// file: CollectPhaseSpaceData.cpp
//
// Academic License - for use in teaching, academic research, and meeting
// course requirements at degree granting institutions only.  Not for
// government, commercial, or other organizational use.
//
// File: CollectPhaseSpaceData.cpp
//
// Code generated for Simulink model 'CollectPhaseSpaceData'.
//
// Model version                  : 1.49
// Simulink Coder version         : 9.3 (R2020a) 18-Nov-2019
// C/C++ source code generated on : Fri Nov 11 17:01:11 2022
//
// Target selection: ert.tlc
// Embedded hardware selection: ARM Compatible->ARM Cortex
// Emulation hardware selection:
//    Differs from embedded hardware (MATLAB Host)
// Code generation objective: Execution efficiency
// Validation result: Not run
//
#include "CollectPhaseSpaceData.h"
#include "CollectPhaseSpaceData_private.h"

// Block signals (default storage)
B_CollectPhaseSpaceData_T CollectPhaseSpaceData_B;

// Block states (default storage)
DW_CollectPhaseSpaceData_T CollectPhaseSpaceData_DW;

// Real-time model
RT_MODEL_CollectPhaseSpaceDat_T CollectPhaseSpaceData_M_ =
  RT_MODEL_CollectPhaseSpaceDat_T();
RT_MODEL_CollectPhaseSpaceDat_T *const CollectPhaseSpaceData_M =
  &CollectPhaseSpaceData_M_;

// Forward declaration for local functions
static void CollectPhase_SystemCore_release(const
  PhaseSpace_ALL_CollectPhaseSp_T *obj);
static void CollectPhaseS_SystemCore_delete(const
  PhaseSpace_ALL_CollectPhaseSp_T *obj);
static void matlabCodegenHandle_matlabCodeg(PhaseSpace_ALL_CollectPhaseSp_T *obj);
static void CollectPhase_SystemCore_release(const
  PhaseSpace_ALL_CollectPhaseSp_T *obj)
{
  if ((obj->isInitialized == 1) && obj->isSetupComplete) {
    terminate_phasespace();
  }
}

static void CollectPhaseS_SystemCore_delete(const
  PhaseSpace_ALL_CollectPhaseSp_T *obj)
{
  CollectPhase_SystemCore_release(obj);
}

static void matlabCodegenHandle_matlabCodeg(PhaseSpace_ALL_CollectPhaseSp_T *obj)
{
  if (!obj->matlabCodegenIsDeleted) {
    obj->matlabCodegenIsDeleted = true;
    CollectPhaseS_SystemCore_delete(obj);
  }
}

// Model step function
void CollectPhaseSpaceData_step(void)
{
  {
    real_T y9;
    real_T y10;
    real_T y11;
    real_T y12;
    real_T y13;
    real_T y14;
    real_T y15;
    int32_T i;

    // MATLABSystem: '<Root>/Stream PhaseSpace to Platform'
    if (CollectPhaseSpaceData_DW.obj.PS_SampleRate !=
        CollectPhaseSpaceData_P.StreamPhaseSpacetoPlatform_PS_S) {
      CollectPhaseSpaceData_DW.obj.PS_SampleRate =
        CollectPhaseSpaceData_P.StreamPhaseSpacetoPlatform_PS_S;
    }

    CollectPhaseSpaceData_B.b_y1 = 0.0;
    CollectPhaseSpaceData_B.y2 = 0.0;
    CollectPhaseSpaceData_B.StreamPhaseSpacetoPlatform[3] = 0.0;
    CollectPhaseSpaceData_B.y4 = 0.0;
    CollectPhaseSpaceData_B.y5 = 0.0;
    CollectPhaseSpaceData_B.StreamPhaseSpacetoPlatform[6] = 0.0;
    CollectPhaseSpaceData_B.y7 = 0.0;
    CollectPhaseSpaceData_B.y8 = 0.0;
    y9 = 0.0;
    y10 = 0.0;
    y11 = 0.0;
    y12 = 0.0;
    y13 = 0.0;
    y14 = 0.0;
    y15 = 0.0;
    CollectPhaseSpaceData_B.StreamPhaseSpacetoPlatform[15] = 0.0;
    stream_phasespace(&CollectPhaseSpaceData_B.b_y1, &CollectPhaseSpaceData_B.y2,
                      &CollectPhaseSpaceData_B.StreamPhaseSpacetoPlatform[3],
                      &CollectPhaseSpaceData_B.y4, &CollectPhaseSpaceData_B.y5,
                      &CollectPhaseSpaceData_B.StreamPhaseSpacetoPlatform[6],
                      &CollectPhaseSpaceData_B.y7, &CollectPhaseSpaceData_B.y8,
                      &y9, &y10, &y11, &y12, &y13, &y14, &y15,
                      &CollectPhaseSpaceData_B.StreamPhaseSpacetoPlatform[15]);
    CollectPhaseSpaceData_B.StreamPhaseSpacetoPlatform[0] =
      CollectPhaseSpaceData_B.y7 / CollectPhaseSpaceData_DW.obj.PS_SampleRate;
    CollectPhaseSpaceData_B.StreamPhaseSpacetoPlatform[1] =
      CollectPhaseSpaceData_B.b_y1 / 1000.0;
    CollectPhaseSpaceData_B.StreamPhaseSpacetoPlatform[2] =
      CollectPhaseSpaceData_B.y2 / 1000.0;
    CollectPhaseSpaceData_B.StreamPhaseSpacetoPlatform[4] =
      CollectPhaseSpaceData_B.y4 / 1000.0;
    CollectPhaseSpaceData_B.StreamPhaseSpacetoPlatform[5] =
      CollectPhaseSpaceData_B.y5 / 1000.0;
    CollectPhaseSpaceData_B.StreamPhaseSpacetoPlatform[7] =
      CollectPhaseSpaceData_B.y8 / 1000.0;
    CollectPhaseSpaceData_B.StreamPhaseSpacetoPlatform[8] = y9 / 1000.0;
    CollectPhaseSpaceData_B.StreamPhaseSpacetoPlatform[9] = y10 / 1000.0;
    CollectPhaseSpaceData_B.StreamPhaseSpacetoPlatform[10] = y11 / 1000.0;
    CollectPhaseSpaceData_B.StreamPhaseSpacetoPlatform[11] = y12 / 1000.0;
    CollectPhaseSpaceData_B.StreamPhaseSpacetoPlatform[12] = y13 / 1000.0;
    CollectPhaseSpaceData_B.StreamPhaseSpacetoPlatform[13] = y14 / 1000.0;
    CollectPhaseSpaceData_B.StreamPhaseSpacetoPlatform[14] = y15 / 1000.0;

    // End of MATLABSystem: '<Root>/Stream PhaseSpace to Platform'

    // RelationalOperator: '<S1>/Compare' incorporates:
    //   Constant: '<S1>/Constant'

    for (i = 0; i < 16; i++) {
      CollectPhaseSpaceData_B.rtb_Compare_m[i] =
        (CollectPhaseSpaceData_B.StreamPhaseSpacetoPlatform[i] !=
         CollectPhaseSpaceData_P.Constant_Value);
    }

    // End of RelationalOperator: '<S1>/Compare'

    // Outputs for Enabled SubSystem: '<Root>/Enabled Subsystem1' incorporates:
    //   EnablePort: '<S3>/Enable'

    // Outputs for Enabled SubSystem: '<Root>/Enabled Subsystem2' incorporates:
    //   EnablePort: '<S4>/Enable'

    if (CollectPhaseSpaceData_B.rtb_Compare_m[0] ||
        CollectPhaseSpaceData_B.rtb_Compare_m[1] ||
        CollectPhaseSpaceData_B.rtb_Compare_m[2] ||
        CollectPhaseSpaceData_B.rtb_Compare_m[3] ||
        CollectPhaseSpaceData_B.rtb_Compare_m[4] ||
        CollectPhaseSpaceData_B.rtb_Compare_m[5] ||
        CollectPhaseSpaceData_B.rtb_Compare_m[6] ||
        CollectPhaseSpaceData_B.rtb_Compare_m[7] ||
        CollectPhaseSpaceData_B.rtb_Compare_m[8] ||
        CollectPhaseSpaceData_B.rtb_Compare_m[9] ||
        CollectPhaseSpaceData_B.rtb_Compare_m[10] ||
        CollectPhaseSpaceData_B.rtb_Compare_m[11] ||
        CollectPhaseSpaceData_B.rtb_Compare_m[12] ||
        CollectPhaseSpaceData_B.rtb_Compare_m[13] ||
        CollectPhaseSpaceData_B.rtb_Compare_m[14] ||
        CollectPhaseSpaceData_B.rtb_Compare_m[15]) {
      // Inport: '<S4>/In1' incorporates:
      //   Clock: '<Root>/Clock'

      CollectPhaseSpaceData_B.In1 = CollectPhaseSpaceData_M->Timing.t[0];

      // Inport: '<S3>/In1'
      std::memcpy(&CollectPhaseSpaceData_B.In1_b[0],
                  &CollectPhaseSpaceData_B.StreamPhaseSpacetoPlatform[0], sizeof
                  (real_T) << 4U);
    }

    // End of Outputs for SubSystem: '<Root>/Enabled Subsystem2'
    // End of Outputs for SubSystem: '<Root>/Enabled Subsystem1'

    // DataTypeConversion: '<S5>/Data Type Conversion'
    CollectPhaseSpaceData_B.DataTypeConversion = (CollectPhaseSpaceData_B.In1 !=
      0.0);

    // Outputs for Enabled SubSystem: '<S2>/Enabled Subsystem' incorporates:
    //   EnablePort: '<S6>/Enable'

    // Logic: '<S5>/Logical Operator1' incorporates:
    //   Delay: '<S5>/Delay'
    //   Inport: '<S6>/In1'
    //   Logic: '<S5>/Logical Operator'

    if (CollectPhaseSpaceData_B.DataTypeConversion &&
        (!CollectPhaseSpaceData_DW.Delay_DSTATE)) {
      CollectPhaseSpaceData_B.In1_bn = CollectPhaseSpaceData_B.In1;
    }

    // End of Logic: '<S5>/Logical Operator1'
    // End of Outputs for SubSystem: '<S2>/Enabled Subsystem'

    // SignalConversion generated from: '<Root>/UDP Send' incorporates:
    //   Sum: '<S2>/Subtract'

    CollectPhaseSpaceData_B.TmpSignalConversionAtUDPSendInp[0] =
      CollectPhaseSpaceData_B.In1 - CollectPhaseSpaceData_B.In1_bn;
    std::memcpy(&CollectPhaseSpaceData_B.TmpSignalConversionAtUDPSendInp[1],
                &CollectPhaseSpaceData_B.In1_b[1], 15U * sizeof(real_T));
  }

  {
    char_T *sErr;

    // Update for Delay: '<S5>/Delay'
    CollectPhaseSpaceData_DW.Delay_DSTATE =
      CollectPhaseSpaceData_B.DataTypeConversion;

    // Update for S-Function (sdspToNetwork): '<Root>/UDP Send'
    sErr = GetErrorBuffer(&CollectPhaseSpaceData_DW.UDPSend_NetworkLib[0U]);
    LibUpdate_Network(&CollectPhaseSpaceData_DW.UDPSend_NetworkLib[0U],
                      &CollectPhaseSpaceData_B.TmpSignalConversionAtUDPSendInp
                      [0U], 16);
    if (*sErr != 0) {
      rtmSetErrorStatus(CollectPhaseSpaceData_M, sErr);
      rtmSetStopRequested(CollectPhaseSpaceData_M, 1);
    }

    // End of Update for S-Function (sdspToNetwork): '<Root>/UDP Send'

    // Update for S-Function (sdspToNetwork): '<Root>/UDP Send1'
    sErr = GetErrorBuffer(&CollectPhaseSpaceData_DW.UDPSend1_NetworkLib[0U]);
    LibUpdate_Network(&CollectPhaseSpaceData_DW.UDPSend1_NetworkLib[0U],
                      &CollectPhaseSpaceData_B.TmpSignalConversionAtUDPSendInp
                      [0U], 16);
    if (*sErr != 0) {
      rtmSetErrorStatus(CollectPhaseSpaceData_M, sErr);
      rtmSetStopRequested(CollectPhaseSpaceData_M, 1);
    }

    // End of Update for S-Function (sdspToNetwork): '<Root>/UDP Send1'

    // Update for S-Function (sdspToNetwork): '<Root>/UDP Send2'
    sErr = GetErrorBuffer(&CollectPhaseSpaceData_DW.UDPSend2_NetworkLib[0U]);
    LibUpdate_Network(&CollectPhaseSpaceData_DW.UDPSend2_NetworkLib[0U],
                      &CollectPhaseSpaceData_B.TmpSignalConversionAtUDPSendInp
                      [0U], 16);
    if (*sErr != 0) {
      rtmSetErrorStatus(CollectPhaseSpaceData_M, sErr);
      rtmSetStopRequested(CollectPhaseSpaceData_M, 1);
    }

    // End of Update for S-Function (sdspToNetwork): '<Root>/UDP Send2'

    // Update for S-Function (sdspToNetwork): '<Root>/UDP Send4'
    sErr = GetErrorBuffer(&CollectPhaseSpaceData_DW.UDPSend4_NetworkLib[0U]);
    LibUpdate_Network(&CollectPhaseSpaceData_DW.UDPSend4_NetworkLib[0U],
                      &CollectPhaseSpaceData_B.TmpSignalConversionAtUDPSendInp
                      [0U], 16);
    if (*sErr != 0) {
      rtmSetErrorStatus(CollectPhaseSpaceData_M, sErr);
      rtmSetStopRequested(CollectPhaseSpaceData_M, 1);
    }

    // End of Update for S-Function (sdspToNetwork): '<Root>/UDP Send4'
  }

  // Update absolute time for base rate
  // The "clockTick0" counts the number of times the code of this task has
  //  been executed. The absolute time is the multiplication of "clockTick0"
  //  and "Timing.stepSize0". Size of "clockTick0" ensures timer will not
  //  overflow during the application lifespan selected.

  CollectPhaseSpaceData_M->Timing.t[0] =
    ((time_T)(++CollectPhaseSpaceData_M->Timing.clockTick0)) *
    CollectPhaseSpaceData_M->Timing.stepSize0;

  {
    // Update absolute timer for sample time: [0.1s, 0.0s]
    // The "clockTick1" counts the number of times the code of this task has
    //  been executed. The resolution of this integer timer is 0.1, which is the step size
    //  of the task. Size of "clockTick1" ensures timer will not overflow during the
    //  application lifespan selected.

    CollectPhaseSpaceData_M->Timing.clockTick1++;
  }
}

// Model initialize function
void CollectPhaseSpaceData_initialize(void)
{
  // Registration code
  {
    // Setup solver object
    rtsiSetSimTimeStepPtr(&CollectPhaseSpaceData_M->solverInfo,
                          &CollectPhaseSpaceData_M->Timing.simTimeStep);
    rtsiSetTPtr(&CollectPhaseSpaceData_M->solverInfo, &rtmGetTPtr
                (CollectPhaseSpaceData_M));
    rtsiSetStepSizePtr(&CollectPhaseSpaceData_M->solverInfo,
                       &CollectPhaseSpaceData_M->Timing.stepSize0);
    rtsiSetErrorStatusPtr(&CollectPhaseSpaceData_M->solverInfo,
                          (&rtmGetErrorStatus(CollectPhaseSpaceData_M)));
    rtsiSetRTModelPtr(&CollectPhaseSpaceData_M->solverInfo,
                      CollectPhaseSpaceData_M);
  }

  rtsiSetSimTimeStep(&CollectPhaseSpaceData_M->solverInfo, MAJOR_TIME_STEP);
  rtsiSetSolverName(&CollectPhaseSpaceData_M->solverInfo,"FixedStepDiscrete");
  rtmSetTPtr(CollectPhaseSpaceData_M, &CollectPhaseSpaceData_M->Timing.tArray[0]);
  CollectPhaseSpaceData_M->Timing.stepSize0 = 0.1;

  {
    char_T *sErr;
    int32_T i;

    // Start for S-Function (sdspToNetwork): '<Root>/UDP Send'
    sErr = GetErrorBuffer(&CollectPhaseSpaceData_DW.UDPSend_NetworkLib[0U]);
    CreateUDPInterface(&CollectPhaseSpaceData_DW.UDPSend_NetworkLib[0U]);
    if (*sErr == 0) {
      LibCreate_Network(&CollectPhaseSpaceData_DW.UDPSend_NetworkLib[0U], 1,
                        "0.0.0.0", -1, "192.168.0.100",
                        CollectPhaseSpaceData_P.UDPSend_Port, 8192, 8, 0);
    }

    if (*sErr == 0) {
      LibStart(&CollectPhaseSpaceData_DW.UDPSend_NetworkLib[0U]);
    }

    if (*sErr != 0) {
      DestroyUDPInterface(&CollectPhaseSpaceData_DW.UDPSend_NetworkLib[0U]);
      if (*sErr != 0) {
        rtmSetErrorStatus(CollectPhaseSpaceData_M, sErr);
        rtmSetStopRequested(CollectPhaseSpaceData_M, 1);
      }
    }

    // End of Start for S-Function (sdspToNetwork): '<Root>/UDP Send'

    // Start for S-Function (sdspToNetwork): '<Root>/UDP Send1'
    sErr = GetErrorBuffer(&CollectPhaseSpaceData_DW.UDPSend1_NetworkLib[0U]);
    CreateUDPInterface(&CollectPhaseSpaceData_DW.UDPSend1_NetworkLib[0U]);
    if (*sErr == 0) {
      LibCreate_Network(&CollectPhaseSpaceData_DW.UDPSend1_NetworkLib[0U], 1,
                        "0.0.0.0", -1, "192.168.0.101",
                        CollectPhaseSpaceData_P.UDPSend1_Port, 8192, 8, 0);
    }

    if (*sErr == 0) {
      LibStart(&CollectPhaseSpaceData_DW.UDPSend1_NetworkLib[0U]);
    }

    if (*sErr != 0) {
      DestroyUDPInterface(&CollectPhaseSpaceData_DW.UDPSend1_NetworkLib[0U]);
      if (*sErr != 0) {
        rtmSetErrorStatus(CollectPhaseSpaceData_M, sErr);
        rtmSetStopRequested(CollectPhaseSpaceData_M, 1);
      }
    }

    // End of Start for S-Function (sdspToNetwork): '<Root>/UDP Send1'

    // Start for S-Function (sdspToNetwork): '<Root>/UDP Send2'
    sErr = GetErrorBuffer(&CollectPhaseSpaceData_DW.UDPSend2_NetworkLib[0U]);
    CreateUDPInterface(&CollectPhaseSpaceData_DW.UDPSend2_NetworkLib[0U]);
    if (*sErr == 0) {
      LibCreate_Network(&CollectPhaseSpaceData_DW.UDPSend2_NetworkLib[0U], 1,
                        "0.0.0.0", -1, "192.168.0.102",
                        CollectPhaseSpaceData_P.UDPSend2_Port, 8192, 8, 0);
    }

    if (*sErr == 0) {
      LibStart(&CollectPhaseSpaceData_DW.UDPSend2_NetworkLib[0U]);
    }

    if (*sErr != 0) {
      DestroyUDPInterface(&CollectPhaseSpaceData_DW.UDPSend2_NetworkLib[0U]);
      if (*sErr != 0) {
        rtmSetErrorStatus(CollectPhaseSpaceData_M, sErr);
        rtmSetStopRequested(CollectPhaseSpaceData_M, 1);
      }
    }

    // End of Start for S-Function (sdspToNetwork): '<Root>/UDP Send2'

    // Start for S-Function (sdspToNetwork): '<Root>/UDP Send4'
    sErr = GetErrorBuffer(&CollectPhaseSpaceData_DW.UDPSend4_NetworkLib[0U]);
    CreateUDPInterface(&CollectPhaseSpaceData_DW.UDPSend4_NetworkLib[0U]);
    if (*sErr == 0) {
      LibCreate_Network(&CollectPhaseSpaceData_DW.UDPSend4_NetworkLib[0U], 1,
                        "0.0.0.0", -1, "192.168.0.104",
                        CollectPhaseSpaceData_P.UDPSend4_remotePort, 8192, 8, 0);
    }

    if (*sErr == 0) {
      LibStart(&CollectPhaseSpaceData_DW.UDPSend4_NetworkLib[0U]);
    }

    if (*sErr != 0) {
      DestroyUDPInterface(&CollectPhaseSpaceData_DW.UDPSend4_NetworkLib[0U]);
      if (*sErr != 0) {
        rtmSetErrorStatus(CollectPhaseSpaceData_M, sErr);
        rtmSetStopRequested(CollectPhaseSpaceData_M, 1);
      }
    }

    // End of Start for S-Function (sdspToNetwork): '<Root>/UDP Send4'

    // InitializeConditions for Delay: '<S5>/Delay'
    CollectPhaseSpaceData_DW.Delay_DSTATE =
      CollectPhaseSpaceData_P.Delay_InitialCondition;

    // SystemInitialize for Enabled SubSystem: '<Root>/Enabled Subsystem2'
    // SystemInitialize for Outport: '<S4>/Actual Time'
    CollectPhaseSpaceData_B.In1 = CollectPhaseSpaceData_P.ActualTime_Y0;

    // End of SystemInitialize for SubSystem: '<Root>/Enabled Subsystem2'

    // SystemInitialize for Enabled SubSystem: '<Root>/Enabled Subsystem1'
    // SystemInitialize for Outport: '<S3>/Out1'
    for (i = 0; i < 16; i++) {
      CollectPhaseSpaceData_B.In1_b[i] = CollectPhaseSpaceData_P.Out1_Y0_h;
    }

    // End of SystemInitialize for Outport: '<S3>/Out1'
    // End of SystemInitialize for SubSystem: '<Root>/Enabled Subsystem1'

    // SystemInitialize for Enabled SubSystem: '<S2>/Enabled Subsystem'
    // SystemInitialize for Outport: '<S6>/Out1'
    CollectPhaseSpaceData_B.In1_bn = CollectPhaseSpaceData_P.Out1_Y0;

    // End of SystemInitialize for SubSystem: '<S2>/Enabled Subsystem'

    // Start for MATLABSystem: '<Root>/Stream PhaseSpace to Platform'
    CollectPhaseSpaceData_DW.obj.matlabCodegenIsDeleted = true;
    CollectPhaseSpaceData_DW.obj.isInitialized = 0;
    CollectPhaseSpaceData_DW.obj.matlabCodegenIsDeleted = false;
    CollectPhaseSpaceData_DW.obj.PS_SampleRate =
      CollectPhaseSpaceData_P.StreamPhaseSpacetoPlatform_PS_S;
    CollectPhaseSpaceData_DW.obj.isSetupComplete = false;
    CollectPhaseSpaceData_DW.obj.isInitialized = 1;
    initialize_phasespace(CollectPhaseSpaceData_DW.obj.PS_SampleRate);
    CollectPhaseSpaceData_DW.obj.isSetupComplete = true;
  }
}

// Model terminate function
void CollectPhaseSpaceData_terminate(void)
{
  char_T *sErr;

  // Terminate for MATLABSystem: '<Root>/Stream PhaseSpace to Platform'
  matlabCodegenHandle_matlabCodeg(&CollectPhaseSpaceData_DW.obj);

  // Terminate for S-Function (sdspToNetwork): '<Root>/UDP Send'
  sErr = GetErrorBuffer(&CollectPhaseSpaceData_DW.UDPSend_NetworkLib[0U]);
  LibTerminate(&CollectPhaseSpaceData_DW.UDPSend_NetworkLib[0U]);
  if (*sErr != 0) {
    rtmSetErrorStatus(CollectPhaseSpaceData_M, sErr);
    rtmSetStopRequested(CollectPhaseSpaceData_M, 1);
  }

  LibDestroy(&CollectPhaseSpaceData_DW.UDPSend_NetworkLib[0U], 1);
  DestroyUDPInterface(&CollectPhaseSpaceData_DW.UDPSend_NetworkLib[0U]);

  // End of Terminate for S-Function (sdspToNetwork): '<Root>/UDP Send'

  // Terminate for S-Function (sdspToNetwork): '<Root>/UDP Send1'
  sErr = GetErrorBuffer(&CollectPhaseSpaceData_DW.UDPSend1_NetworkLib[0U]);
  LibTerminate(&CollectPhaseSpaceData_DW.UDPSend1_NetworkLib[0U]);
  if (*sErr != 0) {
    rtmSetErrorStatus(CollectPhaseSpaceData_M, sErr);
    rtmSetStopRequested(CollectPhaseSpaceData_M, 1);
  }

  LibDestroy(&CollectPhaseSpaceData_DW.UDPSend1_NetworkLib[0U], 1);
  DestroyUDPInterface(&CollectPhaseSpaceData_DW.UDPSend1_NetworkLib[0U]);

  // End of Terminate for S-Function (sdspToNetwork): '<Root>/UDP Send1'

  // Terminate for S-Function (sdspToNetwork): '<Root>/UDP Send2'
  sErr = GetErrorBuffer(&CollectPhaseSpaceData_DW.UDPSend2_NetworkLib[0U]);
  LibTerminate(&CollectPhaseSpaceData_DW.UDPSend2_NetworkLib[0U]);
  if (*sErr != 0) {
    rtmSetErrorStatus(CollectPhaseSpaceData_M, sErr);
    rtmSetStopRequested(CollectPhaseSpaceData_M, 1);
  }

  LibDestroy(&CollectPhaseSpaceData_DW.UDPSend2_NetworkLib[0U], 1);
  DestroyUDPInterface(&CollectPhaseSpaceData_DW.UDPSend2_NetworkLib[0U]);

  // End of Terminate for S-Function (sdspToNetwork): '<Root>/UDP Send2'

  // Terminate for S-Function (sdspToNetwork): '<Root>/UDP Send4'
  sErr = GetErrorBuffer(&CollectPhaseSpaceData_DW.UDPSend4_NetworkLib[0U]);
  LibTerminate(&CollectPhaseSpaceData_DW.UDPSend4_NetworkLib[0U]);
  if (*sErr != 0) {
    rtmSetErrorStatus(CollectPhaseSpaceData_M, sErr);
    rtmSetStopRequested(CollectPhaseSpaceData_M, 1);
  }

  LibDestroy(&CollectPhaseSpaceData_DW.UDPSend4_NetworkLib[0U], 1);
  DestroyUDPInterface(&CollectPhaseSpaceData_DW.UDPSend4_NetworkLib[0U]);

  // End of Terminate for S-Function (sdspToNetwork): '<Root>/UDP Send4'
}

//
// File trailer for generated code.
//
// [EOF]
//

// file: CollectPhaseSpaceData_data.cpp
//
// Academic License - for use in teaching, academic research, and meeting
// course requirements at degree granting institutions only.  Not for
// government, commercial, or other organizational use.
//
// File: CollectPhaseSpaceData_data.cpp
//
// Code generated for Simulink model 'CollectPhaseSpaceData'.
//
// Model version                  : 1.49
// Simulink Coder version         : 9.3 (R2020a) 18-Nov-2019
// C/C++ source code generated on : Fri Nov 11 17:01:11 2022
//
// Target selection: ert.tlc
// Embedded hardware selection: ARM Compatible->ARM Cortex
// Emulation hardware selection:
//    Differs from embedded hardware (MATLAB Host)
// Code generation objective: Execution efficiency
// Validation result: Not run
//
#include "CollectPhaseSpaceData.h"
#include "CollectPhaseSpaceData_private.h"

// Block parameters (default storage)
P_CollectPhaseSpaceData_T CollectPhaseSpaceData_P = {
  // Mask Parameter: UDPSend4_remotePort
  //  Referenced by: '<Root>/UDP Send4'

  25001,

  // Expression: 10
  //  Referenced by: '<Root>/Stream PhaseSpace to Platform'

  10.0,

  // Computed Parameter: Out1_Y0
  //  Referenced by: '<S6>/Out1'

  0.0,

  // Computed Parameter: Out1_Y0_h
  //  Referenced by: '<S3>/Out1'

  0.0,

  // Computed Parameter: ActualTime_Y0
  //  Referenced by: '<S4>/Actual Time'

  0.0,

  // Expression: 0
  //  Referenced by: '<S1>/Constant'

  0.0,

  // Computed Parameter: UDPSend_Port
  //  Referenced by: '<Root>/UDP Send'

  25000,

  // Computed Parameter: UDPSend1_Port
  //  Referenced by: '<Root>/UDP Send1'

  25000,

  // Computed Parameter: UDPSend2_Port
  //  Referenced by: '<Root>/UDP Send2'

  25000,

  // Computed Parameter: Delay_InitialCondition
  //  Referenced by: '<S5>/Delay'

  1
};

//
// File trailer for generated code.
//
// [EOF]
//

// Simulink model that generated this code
simulink model "CollectPhaseSpaceData"  (R2020a)
settings: Solver=FixedStepAuto  StartTime=0.0  StopTime=inf  FixedStep=0.1  RelTol=1e-3  EnableMultiTasking=on
libraries: embdlinuxlib x3, simulink x1, dspswit3 x1, MainLibrary x1, dspnetwork x1

== system CollectPhaseSpaceData ==
  Clock : Clock
  Compare To Zero1 : simulink/Logic and Bit Operations/Compare To Zero  relop=~=  OutDataTypeStr=boolean
  Correct Time : Subsystem
  Data Type Conversion : DataTypeConversion  OutDataTypeStr=double
  Demux1 : Demux  Outputs=[1,15]
  Enabled Subsystem1 : Subsystem  TreatAsAtomicUnit=on
  Enabled Subsystem2 : Subsystem  TreatAsAtomicUnit=on
  Mux1 : Mux  Inputs=2
  Stream PhaseSpace to Platform : MainLibrary/PhaseSpace Functions/Stream PhaseSpace to Platform  PS_SampleRate=10
  Terminator : Terminator
  UDP Send : embdlinuxlib/UDP Send  remoteURL='192.168.0.100'  remotePort=25000  localURL='0.0.0.0'  localPortSource=Automatically determine  localPort=-1  sampletime=-1  blockPlatform=Raspberry Pi  separateLengthPort=0
  UDP Send1 : embdlinuxlib/UDP Send  remoteURL='192.168.0.101'  remotePort=25000  localURL='0.0.0.0'  localPortSource=Automatically determine  localPort=-1  sampletime=-1  blockPlatform=Raspberry Pi  separateLengthPort=0
  UDP Send2 : embdlinuxlib/UDP Send  remoteURL='192.168.0.102'  remotePort=25000  localURL='0.0.0.0'  localPortSource=Automatically determine  localPort=-1  sampletime=-1  blockPlatform=Raspberry Pi  separateLengthPort=0
  UDP Send4 : dspnetwork/UDP Send  remoteURL='192.168.0.104'  remotePort=25001  localURL='0.0.0.0'  localPortSource=Automatically determine  localPort=-1  sendBufferSize=8192  sampletime=-1  blockPlatform=[]  separateLengthPort=0
  wires:
  Demux1/2 -> Mux1/2
  Enabled Subsystem1/1(Out1) -> Demux1/1
  Correct Time/1(Corrected Time) -> Mux1/1
  Demux1/1 -> Terminator/1
  Compare To Zero1/1 -> Enabled Subsystem2/Enable, Enabled Subsystem1/Enable
  Stream PhaseSpace to Platform/1 -> Enabled Subsystem1/1(In1), Compare To Zero1/1
  Enabled Subsystem2/1(Actual Time) -> Correct Time/1(Actual Time)
  Clock/1 -> Enabled Subsystem2/1(In1)
  Mux1/1 -> Data Type Conversion/1, UDP Send2/1, UDP Send1/1, UDP Send/1
  Data Type Conversion/1 -> UDP Send4/1

== system CollectPhaseSpaceData/Correct Time ==
  Actual Time : Inport
  Edge Detector : dspswit3/Edge Detector  InputProcessing=Columns as channels (frame based)
  Enabled Subsystem : Subsystem  TreatAsAtomicUnit=on
  Subtract : Sum  Inputs=+-
  Corrected Time : Outport  VectorParamsAs1DForOutWhenUnconnected=off
  wires:
  Subtract/1 -> Corrected Time/1
  Edge Detector/1 -> Enabled Subsystem/Enable
  Actual Time/1 -> Subtract/1, Enabled Subsystem/1(In1), Edge Detector/1
  Enabled Subsystem/1(Out1) -> Subtract/2

== system CollectPhaseSpaceData/Enabled Subsystem1 ==
  In1 : Inport
  Enable : EnablePort
  Out1 : Outport  VectorParamsAs1DForOutWhenUnconnected=off
  wires:
  In1/1 -> Out1/1

== system CollectPhaseSpaceData/Enabled Subsystem2 ==
  In1 : Inport
  Enable : EnablePort
  Actual Time : Outport  VectorParamsAs1DForOutWhenUnconnected=off
  wires:
  In1/1 -> Actual Time/1

== system CollectPhaseSpaceData/Correct Time/Enabled Subsystem ==
  In1 : Inport
  Enable : EnablePort
  Out1 : Outport  VectorParamsAs1DForOutWhenUnconnected=off
  wires:
  In1/1 -> Out1/1
